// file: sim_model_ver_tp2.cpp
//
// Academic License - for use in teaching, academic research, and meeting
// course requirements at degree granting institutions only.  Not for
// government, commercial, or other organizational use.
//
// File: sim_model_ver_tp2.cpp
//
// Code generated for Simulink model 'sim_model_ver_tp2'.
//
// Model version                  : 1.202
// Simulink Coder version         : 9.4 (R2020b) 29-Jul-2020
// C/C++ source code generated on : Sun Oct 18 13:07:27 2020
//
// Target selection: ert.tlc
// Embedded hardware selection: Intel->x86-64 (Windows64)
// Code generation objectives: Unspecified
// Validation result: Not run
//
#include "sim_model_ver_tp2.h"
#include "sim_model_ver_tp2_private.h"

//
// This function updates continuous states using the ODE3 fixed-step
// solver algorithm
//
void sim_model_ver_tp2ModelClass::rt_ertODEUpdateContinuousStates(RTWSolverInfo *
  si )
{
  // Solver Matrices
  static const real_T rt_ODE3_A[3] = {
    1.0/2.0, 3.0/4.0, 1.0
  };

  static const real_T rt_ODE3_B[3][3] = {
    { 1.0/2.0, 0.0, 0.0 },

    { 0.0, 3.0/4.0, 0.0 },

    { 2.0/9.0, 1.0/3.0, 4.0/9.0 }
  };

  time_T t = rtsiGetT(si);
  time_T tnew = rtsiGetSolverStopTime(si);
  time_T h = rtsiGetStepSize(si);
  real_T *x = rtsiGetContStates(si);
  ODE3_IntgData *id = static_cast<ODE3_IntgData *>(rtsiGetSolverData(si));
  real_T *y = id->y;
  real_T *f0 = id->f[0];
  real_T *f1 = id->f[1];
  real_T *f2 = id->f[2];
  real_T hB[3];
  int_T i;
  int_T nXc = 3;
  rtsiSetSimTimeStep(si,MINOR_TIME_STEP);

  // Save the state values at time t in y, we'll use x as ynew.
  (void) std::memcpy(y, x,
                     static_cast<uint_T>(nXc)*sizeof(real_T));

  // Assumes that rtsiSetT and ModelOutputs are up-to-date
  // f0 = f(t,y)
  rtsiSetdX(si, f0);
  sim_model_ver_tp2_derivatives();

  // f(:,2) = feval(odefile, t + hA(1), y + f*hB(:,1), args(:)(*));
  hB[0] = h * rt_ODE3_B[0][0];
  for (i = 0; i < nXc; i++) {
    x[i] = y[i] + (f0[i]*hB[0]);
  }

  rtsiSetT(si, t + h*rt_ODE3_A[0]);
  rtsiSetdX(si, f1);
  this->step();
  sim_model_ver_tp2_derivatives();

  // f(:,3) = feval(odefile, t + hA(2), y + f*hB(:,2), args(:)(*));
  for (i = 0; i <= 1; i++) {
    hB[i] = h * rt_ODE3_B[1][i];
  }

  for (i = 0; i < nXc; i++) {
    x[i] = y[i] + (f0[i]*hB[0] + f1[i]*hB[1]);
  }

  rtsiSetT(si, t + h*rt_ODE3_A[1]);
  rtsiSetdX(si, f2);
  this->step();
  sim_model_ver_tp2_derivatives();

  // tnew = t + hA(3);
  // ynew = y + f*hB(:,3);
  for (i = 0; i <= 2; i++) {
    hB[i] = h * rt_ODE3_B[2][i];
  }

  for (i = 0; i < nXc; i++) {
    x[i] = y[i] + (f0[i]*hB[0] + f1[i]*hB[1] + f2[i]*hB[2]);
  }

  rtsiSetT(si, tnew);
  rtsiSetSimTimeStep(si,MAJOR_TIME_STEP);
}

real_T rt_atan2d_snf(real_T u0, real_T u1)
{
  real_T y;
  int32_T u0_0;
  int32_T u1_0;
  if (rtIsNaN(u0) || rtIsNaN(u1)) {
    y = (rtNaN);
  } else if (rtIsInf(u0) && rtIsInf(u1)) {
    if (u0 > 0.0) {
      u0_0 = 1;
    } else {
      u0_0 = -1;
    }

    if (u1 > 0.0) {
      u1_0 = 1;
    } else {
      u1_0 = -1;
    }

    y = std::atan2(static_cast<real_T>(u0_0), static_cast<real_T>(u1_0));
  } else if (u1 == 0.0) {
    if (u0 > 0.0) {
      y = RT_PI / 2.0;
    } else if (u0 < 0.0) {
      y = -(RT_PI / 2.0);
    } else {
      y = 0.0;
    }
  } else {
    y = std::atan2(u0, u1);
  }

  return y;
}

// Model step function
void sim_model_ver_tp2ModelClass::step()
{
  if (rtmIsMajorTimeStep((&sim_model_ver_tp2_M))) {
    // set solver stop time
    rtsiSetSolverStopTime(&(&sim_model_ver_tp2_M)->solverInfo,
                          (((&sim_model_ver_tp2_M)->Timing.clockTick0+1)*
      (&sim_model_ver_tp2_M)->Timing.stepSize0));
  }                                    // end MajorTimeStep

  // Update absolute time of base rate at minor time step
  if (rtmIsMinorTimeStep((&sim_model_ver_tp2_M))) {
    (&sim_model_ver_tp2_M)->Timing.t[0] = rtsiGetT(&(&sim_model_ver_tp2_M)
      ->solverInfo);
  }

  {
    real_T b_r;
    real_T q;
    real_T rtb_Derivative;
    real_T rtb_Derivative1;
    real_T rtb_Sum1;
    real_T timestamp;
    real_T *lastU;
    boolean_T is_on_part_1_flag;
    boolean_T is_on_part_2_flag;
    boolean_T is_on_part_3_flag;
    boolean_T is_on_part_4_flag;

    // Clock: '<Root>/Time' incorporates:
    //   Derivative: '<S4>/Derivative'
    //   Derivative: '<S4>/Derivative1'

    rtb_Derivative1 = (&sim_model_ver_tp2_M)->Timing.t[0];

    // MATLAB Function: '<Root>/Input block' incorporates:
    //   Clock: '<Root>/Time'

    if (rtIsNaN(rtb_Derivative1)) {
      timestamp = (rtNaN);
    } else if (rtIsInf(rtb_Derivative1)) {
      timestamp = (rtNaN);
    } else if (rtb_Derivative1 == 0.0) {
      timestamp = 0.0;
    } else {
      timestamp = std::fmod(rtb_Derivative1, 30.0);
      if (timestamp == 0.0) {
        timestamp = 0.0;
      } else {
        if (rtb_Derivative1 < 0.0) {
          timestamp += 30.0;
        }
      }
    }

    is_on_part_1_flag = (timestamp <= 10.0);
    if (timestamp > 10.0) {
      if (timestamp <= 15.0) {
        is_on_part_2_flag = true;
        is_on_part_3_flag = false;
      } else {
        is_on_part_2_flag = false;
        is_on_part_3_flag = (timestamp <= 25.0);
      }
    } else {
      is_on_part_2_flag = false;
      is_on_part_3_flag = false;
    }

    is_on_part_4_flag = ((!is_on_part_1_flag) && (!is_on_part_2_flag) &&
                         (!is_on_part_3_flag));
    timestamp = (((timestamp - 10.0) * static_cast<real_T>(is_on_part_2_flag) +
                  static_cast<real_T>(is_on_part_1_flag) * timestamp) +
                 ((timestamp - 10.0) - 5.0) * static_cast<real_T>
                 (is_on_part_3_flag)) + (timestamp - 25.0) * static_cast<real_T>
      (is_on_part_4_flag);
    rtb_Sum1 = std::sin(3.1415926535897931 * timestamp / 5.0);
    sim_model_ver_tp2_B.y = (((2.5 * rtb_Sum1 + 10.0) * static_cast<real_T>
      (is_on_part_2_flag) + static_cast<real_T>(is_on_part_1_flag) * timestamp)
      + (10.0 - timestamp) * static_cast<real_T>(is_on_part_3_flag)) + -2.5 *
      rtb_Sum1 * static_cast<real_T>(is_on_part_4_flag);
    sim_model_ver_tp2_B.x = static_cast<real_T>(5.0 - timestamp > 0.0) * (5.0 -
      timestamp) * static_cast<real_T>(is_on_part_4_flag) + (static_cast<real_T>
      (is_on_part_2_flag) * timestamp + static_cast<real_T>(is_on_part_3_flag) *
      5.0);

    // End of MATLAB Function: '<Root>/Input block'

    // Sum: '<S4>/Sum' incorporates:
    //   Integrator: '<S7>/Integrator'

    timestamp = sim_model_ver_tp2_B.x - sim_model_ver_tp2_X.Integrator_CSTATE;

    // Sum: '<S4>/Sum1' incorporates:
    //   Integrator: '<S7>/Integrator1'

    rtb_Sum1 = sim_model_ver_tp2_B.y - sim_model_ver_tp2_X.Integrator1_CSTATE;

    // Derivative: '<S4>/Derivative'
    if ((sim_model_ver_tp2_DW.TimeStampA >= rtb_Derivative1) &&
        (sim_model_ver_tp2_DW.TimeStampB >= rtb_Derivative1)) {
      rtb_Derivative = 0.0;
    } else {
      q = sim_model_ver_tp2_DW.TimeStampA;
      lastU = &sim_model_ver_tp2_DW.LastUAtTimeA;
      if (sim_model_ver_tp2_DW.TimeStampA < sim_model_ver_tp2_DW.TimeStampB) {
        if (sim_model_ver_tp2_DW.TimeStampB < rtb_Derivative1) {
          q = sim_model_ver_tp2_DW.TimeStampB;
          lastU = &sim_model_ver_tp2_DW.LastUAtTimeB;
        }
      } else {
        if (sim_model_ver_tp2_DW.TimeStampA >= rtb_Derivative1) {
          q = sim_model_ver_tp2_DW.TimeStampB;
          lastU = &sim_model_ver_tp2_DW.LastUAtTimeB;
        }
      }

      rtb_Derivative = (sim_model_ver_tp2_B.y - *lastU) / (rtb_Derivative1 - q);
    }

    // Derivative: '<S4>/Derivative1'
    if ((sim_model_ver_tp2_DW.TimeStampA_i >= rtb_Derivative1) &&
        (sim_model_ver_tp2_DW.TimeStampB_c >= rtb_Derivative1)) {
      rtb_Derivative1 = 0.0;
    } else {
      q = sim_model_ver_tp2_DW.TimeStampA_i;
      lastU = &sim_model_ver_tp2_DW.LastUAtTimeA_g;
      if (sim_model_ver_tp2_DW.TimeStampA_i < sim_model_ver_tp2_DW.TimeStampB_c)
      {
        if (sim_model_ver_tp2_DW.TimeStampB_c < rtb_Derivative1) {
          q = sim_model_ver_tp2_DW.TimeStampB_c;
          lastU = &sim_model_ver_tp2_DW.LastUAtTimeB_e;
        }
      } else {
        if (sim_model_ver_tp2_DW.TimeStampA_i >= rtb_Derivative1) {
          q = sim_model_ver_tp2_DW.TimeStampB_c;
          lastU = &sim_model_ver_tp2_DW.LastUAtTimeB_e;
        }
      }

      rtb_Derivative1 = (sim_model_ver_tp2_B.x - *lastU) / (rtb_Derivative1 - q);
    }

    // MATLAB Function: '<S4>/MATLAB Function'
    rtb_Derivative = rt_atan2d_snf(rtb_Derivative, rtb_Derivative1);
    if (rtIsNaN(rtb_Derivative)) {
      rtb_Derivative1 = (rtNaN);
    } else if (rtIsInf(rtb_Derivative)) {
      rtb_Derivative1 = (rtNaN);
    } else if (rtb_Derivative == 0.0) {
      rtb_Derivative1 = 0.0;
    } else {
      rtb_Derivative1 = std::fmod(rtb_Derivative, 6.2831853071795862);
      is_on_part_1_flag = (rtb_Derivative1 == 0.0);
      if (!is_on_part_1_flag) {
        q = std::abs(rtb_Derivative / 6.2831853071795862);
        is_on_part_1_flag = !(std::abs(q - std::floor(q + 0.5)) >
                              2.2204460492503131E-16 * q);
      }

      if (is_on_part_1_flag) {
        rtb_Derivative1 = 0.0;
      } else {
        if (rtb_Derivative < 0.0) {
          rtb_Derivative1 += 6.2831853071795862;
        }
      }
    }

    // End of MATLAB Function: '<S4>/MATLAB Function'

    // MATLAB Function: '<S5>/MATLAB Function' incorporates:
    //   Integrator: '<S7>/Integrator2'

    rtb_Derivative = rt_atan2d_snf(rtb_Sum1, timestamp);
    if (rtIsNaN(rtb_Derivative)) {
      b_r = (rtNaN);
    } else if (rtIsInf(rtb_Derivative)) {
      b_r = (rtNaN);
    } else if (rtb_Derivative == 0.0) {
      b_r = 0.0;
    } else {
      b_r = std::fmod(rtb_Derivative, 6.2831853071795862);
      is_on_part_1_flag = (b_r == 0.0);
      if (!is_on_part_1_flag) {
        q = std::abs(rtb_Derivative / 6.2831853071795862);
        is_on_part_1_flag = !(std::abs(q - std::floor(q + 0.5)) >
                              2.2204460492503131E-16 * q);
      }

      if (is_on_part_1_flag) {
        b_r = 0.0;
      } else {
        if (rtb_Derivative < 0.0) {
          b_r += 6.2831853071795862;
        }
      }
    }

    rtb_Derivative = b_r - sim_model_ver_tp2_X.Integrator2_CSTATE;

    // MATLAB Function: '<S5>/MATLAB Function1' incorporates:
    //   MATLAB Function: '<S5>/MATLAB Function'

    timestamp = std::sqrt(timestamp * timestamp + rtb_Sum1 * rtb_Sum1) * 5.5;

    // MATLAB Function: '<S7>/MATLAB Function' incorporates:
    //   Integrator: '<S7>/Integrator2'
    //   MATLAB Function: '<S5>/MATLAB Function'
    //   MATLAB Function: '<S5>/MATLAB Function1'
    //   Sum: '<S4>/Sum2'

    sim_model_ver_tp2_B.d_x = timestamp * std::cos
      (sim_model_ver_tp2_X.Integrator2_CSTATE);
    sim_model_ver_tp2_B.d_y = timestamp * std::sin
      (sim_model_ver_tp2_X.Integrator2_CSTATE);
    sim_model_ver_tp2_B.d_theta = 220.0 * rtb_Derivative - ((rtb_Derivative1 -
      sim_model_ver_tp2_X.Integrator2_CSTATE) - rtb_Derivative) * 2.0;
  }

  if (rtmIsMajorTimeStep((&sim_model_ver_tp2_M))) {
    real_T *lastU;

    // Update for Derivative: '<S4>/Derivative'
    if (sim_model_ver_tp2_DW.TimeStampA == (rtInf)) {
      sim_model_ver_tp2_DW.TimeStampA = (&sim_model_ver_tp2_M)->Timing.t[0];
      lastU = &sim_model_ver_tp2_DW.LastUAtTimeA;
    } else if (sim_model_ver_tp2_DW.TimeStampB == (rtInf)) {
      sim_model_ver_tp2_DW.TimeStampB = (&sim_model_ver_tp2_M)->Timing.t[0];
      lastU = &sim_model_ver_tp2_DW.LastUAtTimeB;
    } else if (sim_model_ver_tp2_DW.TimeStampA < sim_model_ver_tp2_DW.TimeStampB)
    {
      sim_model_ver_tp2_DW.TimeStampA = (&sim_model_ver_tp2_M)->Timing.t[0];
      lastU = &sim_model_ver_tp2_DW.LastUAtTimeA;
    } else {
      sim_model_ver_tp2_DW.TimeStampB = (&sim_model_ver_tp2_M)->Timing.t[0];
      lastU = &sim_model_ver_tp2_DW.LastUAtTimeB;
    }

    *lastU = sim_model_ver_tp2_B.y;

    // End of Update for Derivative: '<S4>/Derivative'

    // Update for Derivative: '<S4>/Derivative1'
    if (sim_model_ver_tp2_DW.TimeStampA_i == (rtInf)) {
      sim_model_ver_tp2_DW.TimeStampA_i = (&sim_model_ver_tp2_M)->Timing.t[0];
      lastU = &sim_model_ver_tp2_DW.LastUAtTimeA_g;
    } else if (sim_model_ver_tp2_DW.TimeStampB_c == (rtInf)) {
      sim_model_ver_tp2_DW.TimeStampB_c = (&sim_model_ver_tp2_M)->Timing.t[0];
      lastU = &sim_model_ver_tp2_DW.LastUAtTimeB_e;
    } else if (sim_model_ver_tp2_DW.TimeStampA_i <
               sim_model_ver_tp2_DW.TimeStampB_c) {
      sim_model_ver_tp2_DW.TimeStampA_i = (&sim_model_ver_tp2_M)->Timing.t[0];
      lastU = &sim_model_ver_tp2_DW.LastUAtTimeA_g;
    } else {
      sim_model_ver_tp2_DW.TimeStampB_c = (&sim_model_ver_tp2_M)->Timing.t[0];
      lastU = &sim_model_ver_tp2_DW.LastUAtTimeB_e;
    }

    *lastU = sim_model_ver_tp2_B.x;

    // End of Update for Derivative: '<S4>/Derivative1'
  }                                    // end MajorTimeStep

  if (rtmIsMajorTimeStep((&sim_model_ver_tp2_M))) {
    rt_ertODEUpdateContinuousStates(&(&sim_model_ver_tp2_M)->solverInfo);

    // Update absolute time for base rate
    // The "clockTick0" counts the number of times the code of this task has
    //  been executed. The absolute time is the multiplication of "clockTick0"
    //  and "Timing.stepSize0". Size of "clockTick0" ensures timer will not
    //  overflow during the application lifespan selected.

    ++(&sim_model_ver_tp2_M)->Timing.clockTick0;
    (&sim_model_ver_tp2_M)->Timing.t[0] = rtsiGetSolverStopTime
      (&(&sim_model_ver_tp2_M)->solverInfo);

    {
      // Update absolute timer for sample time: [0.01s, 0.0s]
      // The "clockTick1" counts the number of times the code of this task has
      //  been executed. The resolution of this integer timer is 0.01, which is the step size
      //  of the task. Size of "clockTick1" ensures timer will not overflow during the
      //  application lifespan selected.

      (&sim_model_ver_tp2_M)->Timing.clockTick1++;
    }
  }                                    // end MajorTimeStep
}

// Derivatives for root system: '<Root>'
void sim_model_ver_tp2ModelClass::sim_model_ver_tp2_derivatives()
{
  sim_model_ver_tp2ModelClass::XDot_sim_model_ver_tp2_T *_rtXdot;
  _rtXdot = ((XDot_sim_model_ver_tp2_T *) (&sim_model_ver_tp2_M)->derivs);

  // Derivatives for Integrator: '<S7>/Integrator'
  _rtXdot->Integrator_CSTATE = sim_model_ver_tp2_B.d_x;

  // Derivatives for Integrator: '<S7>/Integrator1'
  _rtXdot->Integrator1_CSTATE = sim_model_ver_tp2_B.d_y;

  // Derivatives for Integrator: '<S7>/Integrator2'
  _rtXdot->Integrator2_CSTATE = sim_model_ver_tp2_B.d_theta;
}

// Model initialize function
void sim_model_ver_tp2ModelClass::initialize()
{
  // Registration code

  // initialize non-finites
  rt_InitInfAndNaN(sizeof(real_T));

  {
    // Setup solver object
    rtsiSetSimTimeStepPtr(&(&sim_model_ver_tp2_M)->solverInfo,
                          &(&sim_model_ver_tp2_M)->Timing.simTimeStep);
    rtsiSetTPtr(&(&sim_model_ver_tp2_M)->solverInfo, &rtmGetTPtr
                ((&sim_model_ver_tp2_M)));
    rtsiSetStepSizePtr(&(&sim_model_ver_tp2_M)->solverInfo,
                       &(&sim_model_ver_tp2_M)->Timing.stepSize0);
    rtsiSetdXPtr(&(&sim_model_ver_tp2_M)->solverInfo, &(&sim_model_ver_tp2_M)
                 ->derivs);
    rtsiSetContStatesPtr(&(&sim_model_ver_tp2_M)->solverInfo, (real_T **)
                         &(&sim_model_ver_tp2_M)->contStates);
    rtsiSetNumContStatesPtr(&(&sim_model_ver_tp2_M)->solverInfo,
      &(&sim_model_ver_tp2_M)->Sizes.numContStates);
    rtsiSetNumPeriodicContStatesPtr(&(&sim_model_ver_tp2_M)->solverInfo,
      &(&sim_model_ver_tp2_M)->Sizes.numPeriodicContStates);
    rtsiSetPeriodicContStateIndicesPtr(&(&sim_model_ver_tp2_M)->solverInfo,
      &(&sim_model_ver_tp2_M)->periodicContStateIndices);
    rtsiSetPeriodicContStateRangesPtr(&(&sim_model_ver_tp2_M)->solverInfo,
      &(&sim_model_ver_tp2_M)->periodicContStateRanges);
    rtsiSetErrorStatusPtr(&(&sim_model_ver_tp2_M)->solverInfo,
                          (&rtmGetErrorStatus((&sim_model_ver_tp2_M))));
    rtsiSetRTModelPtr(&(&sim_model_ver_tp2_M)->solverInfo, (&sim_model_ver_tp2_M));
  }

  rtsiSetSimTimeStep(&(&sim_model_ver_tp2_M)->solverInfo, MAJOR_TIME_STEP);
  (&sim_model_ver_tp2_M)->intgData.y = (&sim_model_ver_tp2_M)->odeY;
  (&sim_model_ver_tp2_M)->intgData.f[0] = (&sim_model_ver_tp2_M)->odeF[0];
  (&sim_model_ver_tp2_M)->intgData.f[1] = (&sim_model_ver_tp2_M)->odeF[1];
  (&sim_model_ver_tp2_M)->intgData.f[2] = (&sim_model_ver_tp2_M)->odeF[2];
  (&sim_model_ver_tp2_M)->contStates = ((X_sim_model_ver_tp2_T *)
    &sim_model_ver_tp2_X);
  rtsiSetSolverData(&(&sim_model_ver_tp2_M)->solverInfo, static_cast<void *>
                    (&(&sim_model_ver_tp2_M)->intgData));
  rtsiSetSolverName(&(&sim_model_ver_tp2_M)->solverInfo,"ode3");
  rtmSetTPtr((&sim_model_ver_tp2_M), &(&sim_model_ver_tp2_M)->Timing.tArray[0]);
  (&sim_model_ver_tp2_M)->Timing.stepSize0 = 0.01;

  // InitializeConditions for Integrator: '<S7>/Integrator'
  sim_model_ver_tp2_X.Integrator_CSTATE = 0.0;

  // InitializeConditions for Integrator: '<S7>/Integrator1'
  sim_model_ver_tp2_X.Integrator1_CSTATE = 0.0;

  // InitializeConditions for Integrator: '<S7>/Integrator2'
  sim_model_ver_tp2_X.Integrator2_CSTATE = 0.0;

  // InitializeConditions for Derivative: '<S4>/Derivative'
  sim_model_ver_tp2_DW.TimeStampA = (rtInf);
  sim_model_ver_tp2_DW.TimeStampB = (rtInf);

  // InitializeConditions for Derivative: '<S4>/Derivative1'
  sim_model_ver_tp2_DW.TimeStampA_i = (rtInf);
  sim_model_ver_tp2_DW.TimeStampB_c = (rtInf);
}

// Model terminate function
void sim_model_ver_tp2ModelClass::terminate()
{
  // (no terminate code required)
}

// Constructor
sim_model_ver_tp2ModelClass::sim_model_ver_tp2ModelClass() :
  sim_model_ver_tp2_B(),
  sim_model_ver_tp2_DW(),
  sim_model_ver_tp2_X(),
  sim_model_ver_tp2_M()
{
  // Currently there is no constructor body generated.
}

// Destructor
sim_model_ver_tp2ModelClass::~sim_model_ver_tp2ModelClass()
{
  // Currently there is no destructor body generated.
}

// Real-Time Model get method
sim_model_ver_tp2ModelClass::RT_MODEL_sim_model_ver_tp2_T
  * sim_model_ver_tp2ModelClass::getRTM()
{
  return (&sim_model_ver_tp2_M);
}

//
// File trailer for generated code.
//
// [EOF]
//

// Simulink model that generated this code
simulink model "sim_model_ver_tp2"  (R2020a)
settings: Solver=FixedStepAuto  StartTime=0.0  StopTime=45  FixedStep=0.01  RelTol=1e-3
libraries: simulink x2

== system sim_model_ver_tp2 ==
  Dashboard Scope{,1..3} (4 alike) : DashboardScope
  Input : simulink/Sinks/XY Graph  xmin=-1  xmax=5.5  ymin=-5  ymax=13  st=-1
  Input block : MATLAB Function  TreatAsAtomicUnit=on
  Output : simulink/Sinks/XY Graph  xmin=-1  xmax=5.5  ymin=-5  ymax=13  st=-1
  Speed : Constant
  System : Subsystem
  Time : Clock
  wires:
  System/1(x) -> Output/1  "x_out"
  System/2(y) -> Output/2  "y_out"
  Input block/1(x) -> Input/1, System/1(xr)  "x_in"
  Input block/2(y) -> System/2(yr), Input/2  "y_in"
  Speed/1 -> Input block/2(v)
  Time/1 -> Input block/1(t)

== system sim_model_ver_tp2/System ==
  xr : Inport
  yr : Inport  Port=2
  Control block : Subsystem
  Derivative : Derivative
  Derivative1 : Derivative
  MATLAB Function : MATLAB Function  TreatAsAtomicUnit=on
  Sum : Sum  Inputs=|+-
  Sum1 : Sum  Inputs=|+-
  Sum2 : Sum  Inputs=|+-
  System block : Subsystem
  x : Outport  VectorParamsAs1DForOutWhenUnconnected=off
  y : Outport  Port=2  VectorParamsAs1DForOutWhenUnconnected=off
  wires:
  Sum1/1 -> Control block/2(e_y)
  Control block/2(w) -> System block/2(w)
  Derivative/1 -> MATLAB Function/1(d_y)
  MATLAB Function/1(theta_r) -> Sum2/1
  System block/2(y) -> y/1, Sum1/2
  System block/3(theta) -> Control block/4(theta), Sum2/2
  System block/1(x) -> x/1, Sum/2
  Derivative1/1 -> MATLAB Function/2(d_x)
  Sum/1 -> Control block/1(e_x)
  Control block/1(v) -> System block/1(v)
  Sum2/1 -> Control block/3(theta_e)
  yr/1 -> Derivative/1, Sum1/1
  xr/1 -> Sum/1, Derivative1/1

== system sim_model_ver_tp2/System/Control block ==
  e_x : Inport
  e_y : Inport  Port=2
  theta_e : Inport  Port=3
  theta : Inport  Port=4
  MATLAB Function : MATLAB Function  TreatAsAtomicUnit=on
  MATLAB Function1 : MATLAB Function  TreatAsAtomicUnit=on
  v : Outport  VectorParamsAs1DForOutWhenUnconnected=off
  w : Outport  Port=2  VectorParamsAs1DForOutWhenUnconnected=off
  wires:
  MATLAB Function1/1(v) -> v/1
  MATLAB Function1/2(w) -> w/1
  e_x/1 -> MATLAB Function/1(e_x)
  e_y/1 -> MATLAB Function/2(e_y)
  theta_e/1 -> MATLAB Function/4(theta_e)
  MATLAB Function/1(L) -> MATLAB Function1/1(L)
  MATLAB Function/2(alpha) -> MATLAB Function1/2(alpha)
  MATLAB Function/3(beta) -> MATLAB Function1/3(beta)
  theta/1 -> MATLAB Function/3(theta)

== system sim_model_ver_tp2/System/System block ==
  v : Inport
  w : Inport  Port=2
  Integrator : Integrator
  Integrator1 : Integrator
  Integrator2 : Integrator
  MATLAB Function : MATLAB Function  TreatAsAtomicUnit=on
  x : Outport  VectorParamsAs1DForOutWhenUnconnected=off
  y : Outport  Port=2  VectorParamsAs1DForOutWhenUnconnected=off
  theta : Outport  Port=3  VectorParamsAs1DForOutWhenUnconnected=off
  wires:
  Integrator2/1 -> theta/1, MATLAB Function/3(theta)  "theta"
  MATLAB Function/1(d_x) -> Integrator/1
  MATLAB Function/3(d_theta) -> Integrator2/1
  v/1 -> MATLAB Function/1(v)
  MATLAB Function/2(d_y) -> Integrator1/1
  Integrator/1 -> x/1  "x"
  w/1 -> MATLAB Function/2(w)
  Integrator1/1 -> y/1  "y"

== matlab function sim_model_ver_tp2/System/Control block/MATLAB Function ==
function [L , alpha, beta] = to_parameters(e_x , e_y , theta , theta_e)
    L = sqrt(e_x * e_x + e_y * e_y);
    alpha = mod(atan2(e_y , e_x) , 2*pi) - theta;
    beta = theta_e - alpha;
end

== matlab function sim_model_ver_tp2/System/System block/MATLAB Function ==
function [d_x,  d_y,  d_theta] = system(v , w , theta)

    d_x = v*cos(theta);
    d_y = v*sin(theta);
    d_theta = w;

end

== matlab function sim_model_ver_tp2/System/Control block/MATLAB Function1 ==
function [v , w] = to_v_w(L, alpha , beta)

%old
% k_L = -3;
% k_alpha = -210;
% k_beta = 4.5;

k_L = -5.5;
k_alpha = -220;
k_beta = 2;

v = -k_L * L;
w = -k_alpha * alpha - k_beta * beta;

end

== matlab function sim_model_ver_tp2/System/MATLAB Function ==
function theta_r = arctan2(d_y , d_x)
    theta_r = mod(atan2(d_y , d_x) , 2*pi);
end

== matlab function sim_model_ver_tp2/Input block ==
function [x , y] = input(t , v)

    h = 10; %Straight line distance
    d = 5; %"Circle" diameter

    
    t = (mod(t , 2*h/v + 2*(d/v))); %% Loop

    is_on_part_1_flag = (t <= h/v);
    is_on_part_2_flag = (t > h/v && t <= h/v + d/v);
    is_on_part_3_flag = (t > h/v + d/v && t <= (2*h/v)+d/v); 
    is_on_part_4_flag = (~is_on_part_1_flag &&...
                         ~is_on_part_2_flag &&...
                         ~is_on_part_3_flag);
    
    timestamp = (is_on_part_1_flag) * t +...
                (is_on_part_2_flag) * (t - h/v) + ... 
                (is_on_part_3_flag) * (t - h/v - d/v)+...
                (is_on_part_4_flag) * (t - (2*h/v + (d/v)));

    y = is_on_part_1_flag * (timestamp*v)+...
        is_on_part_2_flag * (h + (d/2) * sin(pi*timestamp*v/d))+... 
        is_on_part_3_flag * (h-timestamp*v)+...
        is_on_part_4_flag * (-(d/2) * sin(pi*timestamp*v/d));

        
    x = is_on_part_1_flag * (0)+...
        is_on_part_2_flag * (timestamp*v)+... 
        is_on_part_3_flag * (d)+...
        is_on_part_4_flag * ((d - timestamp*v >0)*(d - timestamp*v));

            
            

end
